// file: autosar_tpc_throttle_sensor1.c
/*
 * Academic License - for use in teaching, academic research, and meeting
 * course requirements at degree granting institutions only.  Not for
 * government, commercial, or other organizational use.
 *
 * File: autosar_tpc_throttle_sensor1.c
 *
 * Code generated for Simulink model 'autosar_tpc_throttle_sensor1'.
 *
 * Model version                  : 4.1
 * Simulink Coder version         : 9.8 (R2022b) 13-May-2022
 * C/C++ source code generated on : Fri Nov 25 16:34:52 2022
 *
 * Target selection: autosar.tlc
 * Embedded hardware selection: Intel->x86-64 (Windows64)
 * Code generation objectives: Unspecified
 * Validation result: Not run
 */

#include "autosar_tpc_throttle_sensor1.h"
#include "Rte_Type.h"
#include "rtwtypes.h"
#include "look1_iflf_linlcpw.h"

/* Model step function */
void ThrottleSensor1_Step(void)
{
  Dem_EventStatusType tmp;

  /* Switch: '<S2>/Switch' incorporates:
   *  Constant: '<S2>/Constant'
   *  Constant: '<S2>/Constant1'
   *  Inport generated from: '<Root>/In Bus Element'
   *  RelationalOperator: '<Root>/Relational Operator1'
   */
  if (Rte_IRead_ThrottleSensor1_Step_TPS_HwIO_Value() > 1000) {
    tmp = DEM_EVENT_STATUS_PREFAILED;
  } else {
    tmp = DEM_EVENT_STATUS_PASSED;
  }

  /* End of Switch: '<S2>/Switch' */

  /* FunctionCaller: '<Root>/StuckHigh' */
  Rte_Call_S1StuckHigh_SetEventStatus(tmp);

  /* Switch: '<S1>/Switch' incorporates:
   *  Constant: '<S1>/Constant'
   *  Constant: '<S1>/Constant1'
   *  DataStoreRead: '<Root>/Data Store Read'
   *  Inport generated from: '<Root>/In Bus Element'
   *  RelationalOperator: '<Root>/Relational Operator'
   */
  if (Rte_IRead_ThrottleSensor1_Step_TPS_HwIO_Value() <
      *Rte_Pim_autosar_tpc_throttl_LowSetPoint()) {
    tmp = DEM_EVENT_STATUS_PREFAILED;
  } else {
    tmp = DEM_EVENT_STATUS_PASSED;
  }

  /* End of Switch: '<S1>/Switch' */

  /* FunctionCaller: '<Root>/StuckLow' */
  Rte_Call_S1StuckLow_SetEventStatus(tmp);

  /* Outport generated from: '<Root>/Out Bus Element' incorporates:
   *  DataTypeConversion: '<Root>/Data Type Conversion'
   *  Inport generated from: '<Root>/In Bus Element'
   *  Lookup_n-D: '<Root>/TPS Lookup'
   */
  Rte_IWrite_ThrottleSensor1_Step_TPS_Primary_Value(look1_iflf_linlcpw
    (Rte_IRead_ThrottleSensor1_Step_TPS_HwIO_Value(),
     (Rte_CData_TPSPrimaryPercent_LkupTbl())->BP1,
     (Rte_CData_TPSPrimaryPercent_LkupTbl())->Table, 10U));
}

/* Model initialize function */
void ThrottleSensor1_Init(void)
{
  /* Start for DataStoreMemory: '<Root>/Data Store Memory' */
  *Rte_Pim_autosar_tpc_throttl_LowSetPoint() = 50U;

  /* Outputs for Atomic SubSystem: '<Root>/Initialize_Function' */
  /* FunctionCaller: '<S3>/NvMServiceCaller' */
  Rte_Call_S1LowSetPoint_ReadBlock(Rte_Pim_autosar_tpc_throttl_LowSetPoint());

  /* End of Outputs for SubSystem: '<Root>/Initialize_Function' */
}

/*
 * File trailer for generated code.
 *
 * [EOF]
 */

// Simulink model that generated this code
simulink model "autosar_tpc_throttle_sensor1"  (R2022a)
settings: Solver=FixedStepDiscrete  StartTime=0.0  StopTime=10.0  FixedStep=0.005  RelTol=1e-3
model workspace (MAT data in the model file):
  TPSPrimaryPercent_LkupTbl : Simulink.LookupTable (value not decoded)
undefined symbols (not defined in the file or in its folder): Dem_EventStatusType, TPSPercentBkpt, TPSPercentTbl
libraries: autosarlibdem x2, autosarlibnvm x1

== system autosar_tpc_throttle_sensor1 ==
  note: Copyright 2019-2020 The MathWorks, Inc.
  In Bus Element : Inport  PortName=TPS_HwIO  Element=Value
  BoolToEventStatus : Subsystem
  BoolToEventStatus1 : Subsystem
  Constant1 : Constant  Value=1000
  Data Store Memory : DataStoreMemory  DataStoreName=LowSetPoint  InitialValue=50  ShowAdditionalParam=off
  Data Store Read : DataStoreRead  DataStoreName=LowSetPoint  IndexOptions=Index vector (dialog)  Indices=1  OutputSizes=1
  Data Type Conversion : DataTypeConversion  OutDataTypeStr=single  SaturateOnIntegerOverflow=off  RndMeth=Floor
  Initialize_Function : Subsystem  TreatAsAtomicUnit=on
  Relational Operator : RelationalOperator  Operator=<  OutDataTypeStr=boolean  InputSameDT=off
  Relational Operator1 : RelationalOperator  Operator=>  OutDataTypeStr=boolean  InputSameDT=off
  StuckHigh : autosarlibdem/DiagnosticMonitorCaller  PortName=S1StuckHigh  Operation=SetEventStatus  Datatype=Enum: Dem_EventStatusType  st=-1  ServiceImpl=autosar.bsw.DemDiagnosticMonitor
  StuckLow : autosarlibdem/DiagnosticMonitorCaller  PortName=S1StuckLow  Operation=SetEventStatus  Datatype=Enum: Dem_EventStatusType  st=-1  ServiceImpl=autosar.bsw.DemDiagnosticMonitor
  TPS Lookup : Lookup_n-D  NumberOfTableDimensions=1  DataSpecification=Lookup table object  LookupTableObject=TPSPrimaryPercent_LkupTbl  BreakpointsForDimension1=TPSPercentBkpt  BreakpointsForDimension1DataTypeStr=single  IndexSearchMethod=Linear search  Table=TPSPercentTbl  TableDataTypeStr=single  ExtrapMethod=Clip  InternalRulePriority=Speed  OutDataTypeStr=single  RndMeth=Simplest
  Terminator : Terminator
  Terminator1 : Terminator
  Out Bus Element : Outport  VectorParamsAs1DForOutWhenUnconnected=off  PortName=TPS_Primary  Element=Value
  Scope : Scope
  wires:
  TPS Lookup/1 -> Out Bus Element/1
  Data Type Conversion/1 -> TPS Lookup/1
  In Bus Element/1 -> Relational Operator1/1, Relational Operator/1, Data Type Conversion/1
  StuckLow/1 -> Terminator/1
  Constant1/1 -> Relational Operator1/2
  StuckHigh/1 -> Terminator1/1
  BoolToEventStatus/1(EventStatus) -> StuckLow/1
  Data Store Read/1 -> Relational Operator/2
  Relational Operator1/1 -> BoolToEventStatus1/1(FailCondition)
  Relational Operator/1 -> BoolToEventStatus/1(FailCondition)
  BoolToEventStatus1/1(EventStatus) -> StuckHigh/1

== system autosar_tpc_throttle_sensor1/BoolToEventStatus ==
  FailCondition : Inport
  Constant : Constant  Value=Dem_EventStatusType.DEM_EVENT_STATUS_PASSED
  Constant1 : Constant  Value=Dem_EventStatusType.DEM_EVENT_STATUS_PREFAILED
  Switch : Switch  Criteria=u2 ~= 0  SaturateOnIntegerOverflow=off  InputSameDT=off
  EventStatus : Outport  VectorParamsAs1DForOutWhenUnconnected=off
  wires:
  FailCondition/1 -> Switch/2
  Constant/1 -> Switch/3
  Constant1/1 -> Switch/1
  Switch/1 -> EventStatus/1

== system autosar_tpc_throttle_sensor1/BoolToEventStatus1 ==
  FailCondition : Inport
  Constant : Constant  Value=Dem_EventStatusType.DEM_EVENT_STATUS_PASSED
  Constant1 : Constant  Value=Dem_EventStatusType.DEM_EVENT_STATUS_PREFAILED
  Switch : Switch  Criteria=u2 ~= 0  SaturateOnIntegerOverflow=off  InputSameDT=off
  EventStatus : Outport  VectorParamsAs1DForOutWhenUnconnected=off
  wires:
  Switch/1 -> EventStatus/1
  Constant1/1 -> Switch/1
  Constant/1 -> Switch/3
  FailCondition/1 -> Switch/2

== system autosar_tpc_throttle_sensor1/Initialize_Function ==
  Data Store Write : DataStoreWrite  DataStoreName=LowSetPoint  IndexOptions=Index vector (dialog)  Indices=1  OutputSizes=1
  Event Listener : EventListener  DisableCoverage=on  EventName=reset
  NvMServiceCaller : autosarlibnvm/NvMServiceCaller  PortName=S1LowSetPoint  Operation=ReadBlock  ArgumentSpecification=uint8(1)  st=-1  ServiceImpl=autosar.bsw.NvMService
  Terminator : Terminator
  wires:
  NvMServiceCaller/2 -> Terminator/1
  NvMServiceCaller/1 -> Data Store Write/1
